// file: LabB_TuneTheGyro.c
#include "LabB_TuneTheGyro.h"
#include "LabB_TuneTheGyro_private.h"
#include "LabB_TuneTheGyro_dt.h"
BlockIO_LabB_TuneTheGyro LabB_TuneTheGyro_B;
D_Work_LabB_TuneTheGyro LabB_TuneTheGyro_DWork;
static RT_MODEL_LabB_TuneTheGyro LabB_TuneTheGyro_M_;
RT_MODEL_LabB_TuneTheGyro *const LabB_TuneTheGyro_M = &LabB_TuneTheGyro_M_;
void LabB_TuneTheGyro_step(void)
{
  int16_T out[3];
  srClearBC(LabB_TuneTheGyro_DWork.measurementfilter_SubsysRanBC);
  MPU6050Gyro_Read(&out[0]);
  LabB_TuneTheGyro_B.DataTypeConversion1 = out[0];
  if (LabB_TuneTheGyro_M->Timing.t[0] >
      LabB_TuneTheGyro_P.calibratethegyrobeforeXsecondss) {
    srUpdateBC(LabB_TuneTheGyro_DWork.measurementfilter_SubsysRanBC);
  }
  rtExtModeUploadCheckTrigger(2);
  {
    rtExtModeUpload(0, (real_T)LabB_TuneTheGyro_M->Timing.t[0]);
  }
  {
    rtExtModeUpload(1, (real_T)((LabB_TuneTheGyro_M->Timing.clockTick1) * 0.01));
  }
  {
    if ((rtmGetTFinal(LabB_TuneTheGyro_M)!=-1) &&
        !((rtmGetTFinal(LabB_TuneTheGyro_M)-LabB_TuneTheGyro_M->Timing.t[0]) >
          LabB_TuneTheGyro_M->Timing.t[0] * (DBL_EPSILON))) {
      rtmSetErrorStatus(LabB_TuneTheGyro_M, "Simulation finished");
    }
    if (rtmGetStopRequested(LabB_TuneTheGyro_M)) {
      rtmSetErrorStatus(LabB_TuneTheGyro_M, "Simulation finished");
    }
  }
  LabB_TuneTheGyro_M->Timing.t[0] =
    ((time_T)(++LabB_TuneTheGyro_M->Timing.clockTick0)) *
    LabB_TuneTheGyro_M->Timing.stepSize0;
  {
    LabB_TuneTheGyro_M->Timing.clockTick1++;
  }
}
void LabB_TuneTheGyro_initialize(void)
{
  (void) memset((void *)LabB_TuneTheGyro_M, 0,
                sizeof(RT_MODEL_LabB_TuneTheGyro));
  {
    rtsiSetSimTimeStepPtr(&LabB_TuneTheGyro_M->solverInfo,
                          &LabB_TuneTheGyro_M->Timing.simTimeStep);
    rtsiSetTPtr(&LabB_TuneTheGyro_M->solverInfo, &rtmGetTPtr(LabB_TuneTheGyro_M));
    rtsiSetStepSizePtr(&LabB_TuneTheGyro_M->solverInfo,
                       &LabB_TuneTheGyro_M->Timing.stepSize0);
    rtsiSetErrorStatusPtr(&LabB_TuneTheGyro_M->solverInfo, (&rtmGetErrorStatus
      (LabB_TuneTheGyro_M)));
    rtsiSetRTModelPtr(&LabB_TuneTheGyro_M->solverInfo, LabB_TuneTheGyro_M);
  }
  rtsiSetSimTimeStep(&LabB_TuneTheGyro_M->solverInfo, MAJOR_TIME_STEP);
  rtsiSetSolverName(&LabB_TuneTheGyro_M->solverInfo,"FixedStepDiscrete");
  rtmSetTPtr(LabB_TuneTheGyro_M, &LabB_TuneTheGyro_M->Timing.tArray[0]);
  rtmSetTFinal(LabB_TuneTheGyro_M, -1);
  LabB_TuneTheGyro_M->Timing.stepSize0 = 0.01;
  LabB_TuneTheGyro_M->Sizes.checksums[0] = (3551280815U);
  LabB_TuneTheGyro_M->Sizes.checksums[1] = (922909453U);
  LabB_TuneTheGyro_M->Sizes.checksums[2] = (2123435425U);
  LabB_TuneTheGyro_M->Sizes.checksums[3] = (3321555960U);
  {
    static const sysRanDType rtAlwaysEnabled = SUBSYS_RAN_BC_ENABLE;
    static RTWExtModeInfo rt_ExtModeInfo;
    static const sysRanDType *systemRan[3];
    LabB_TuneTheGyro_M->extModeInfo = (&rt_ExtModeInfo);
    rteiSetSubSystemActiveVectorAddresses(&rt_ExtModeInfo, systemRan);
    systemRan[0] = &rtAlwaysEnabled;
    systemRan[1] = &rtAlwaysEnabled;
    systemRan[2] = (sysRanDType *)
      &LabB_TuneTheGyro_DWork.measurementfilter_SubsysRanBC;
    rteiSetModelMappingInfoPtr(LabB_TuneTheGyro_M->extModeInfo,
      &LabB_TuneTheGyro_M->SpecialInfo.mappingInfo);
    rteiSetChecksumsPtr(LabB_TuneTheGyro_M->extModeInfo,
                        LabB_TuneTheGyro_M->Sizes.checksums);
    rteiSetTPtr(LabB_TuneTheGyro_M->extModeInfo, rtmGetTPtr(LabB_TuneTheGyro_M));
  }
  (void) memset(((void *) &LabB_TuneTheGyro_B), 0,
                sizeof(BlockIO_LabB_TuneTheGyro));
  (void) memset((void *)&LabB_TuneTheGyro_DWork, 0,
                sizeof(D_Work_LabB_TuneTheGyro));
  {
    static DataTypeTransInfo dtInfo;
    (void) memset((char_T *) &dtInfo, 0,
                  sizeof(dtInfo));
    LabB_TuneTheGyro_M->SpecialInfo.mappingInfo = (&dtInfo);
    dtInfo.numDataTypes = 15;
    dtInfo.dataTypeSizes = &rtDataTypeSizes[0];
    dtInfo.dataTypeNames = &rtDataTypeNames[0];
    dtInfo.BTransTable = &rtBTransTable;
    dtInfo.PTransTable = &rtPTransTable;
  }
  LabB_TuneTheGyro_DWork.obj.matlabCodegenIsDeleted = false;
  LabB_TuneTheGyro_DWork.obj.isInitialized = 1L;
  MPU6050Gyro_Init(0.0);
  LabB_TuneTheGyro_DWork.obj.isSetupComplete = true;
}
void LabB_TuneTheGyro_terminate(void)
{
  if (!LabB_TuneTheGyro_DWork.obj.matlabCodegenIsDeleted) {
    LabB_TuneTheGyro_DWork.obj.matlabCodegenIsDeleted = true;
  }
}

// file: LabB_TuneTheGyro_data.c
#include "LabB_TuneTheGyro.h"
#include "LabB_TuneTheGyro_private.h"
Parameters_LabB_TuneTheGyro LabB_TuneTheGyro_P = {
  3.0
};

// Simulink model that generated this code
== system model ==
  measurementfilter : Subsystem  <- 1: DataTypeConversion1, Enable: CompareToConstant#1
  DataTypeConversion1 : DataTypeConversion  <- 1: MATLABSystem#1
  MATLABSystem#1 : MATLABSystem
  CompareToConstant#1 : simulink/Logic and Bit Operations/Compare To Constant  relop=>  const=3  <- 1: Clock#1
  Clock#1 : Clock
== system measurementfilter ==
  Inport#1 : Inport
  EnablePort#1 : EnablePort
